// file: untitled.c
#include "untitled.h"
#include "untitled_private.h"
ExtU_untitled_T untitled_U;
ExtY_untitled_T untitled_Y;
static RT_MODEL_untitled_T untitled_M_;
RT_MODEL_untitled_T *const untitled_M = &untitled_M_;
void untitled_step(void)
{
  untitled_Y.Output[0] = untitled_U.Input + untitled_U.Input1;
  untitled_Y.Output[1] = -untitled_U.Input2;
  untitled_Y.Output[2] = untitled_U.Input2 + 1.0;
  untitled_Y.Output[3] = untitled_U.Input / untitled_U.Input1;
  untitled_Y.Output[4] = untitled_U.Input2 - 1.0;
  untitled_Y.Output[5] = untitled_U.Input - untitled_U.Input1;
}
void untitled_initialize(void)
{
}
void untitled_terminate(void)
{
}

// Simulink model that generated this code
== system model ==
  Input : Inport
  Input1 : Inport
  Input2 : Inport
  Output : Outport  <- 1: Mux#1
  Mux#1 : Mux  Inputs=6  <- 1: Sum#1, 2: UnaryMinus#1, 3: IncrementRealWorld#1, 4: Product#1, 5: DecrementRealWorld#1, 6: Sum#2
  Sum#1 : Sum  <- 1: Input, 2: Input1
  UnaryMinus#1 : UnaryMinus  <- 1: Input2
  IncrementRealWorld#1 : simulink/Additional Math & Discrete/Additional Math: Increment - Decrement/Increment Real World  <- 1: Input2
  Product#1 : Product  Inputs=*/  <- 1: Input, 2: Input1
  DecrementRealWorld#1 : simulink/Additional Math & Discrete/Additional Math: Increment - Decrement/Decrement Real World  <- 1: Input2
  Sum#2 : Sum  Inputs=+-  <- 1: Input, 2: Input1
